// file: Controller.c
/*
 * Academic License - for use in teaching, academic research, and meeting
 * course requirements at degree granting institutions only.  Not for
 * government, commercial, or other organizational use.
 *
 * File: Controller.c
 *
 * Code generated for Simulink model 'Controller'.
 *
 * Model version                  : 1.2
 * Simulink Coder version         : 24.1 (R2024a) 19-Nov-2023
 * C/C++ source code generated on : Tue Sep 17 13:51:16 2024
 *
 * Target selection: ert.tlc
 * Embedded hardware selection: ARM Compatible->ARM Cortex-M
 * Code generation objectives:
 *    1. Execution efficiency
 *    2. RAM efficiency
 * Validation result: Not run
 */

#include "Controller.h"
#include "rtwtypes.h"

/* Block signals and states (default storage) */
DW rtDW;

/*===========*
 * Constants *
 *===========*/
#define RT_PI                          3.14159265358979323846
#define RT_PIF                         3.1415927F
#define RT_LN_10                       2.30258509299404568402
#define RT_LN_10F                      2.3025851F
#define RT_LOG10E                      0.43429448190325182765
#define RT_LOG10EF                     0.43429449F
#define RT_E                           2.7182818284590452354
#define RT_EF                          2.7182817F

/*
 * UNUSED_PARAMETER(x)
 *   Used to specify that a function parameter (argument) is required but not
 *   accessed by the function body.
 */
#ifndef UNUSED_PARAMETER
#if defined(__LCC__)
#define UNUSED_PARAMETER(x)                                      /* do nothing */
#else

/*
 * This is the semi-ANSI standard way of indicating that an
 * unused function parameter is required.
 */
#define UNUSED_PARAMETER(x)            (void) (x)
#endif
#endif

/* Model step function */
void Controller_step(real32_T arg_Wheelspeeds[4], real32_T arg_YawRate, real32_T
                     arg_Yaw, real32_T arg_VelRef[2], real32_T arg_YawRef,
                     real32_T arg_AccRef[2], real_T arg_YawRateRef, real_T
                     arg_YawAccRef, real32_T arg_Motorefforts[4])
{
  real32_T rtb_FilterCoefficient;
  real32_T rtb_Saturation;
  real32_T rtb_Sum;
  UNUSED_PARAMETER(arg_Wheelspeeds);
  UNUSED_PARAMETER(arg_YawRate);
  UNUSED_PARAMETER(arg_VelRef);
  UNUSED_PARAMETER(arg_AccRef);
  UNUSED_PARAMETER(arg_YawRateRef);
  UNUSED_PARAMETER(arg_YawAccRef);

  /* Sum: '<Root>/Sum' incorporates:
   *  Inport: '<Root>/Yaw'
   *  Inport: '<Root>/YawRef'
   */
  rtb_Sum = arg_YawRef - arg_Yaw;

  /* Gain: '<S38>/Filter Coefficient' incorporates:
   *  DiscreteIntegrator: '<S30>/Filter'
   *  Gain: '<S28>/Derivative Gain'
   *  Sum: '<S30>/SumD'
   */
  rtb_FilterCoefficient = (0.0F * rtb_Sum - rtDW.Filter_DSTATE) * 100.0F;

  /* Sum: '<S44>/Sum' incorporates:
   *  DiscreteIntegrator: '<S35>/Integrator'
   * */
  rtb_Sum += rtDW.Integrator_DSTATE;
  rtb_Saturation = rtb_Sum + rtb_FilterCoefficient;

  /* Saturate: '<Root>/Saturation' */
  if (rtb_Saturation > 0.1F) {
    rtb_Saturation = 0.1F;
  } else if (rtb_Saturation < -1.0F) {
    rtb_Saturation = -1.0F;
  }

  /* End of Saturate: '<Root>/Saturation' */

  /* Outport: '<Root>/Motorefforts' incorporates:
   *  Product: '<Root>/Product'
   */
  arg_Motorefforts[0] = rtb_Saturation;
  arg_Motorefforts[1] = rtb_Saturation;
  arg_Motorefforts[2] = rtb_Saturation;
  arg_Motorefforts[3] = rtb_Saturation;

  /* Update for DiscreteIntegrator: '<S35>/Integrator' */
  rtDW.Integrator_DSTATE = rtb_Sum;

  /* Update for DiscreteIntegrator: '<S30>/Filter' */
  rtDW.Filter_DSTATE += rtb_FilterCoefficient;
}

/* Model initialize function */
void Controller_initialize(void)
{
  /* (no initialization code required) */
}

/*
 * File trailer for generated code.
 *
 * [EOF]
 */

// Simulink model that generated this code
simulink model "Controller"  (R2024a)
settings: Solver=VariableStepAuto  StartTime=0.0  StopTime=10.0  RelTol=1e-3
libraries: slpidlib x1

== system Controller ==
  note: Reference
  note: Sensor inputs
  Wheelspeeds : Inport  OutDataTypeStr=single  Unit=rad/s  PortDimensions=4  LockScale=on
  YawRate : Inport  Port=2  OutDataTypeStr=single  Unit=rad/s  PortDimensions=1
  Yaw : Inport  Port=3  OutDataTypeStr=single  Unit=rad  PortDimensions=1
  VelRef : Inport  Port=4  OutDataTypeStr=single  Unit=m/s  PortDimensions=2
  YawRef : Inport  Port=5
  AccRef : Inport  Port=6  OutDataTypeStr=single  Unit=m/s^2  PortDimensions=2
  YawRateRef : Inport  Port=7
  YawAccRef : Inport  Port=8
  Discrete PID Controller : slpidlib/PID Controller  Controller=PID  Form=Parallel  TimeDomain=Discrete-time  UseExternalTs=off  SampleTime=-1  IntegratorMethod=Forward Euler  FilterMethod=Forward Euler  ControllerParametersSource=internal  P=1  I=1  UseKiTs=off  D=0  UseExternalDerivativeSource=off  N=100  UseFilter=on  TunerSelectOption=Transfer Function Based (PID Tuner App)  InitialConditionSource=internal  InitialConditionForIntegrator=0  InitialConditionForFilter=0  DifferentiatorICPrevScaledInput=0  ExternalReset=none  TrackingMode=off  Kt=1  LimitOutput=off  SatLimitsSource=internal  UpperSaturationLimit=inf  LowerSaturationLimit=-inf  LinearizeAsGain=off  AntiWindupMode=none  Kb=1  LimitIntegrator=off  UpperIntegratorSaturationLimit=inf  LowerIntegratorSaturationLimit=-inf  POutMin=[]  POutMax=[]  IOutMin=[]  IOutMax=[]  DOutMin=[]  DOutMax=[]  NOutMin=[]  NOutMax=[]  SumOutMin=[]  SumOutMax=[]  SaturationOutMin=[]  SaturationOutMax=[]  PParamMin=[]  PParamMax=[]  IParamMin=[]  IParamMax=[]  DParamMin=[]  DParamMax=[]  NParamMin=[]  NParamMax=[]  KbParamMin=[]  KbParamMax=[]  KtParamMin=[]  KtParamMax=[]  KbOutMin=[]  KbOutMax=[]  KtOutMin=[]  KtOutMax=[]  IntegratorOutMin=[]  IntegratorOutMax=[]  FilterOutMin=[]  FilterOutMax=[]  SumI1OutMin=[]  SumI1OutMax=[]  SumI2OutMin=[]  SumI2OutMax=[]  SumI3OutMin=[]  SumI3OutMax=[]  SumI4OutMin=[]  SumI4OutMax=[]  SumDOutMin=[]  SumDOutMax=[]  DifferentiatorOutMin=[]  DifferentiatorOutMax=[]  FilterDiffOutCoefMin=[]  FilterDiffOutCoefMax=[]  ReciprocalOutMin=[]  ReciprocalOutMax=[]  SumDenOutMin=[]  SumDenOutMax=[]  SumNumOutMin=[]  SumNumOutMax=[]  DivideOutMin=[]  DivideOutMax=[]  UdiffTsProdOutMin=[]  UdiffTsProdOutMax=[]  NTsProdOutMin=[]  NTsProdOutMax=[]  UintegralTsProdOutMin=[]  UintegralTsProdOutMax=[]  UngainTsProdOutMin=[]  UngainTsProdOutMax=[]  ClampingZeroOutDataTypeStr=Inherit: Inherit via back propagation  ClampingZeroOutMin=[]  ClampingZeroOutMax=[]  FilterDenConstantOutDataTypeStr=Inherit: Inherit via back propagation  FilterDenConstantOutMin=[]  FilterDenConstantOutMax=[]  PCopyOutDataTypeStr=Inherit: Inherit via back propagation  PCopyOutMin=[]  PCopyOutMax=[]  NCopyOutDataTypeStr=Inherit: Inherit via back propagation  NCopyOutMin=[]  NCopyOutMax=[]  IntegratorContinuousStateAttributes=''  IntegratorStateMustResolveToSignalObject=off  IntegratorRTWStateStorageClass=Auto  FilterContinuousStateAttributes=''  FilterStateMustResolveToSignalObject=off  FilterRTWStateStorageClass=Auto  ParallelPVariant=InternalParameters  IdealPVariant=Disabled  IVariant=InternalParameters  DVariant=InternalParameters  IntegratorVariant=Discrete  SatVariant=Disabled  AWVariant=Passthrough  PCopyVariant=Disabled  TRVariant=Disabled  FdbkBlocksVariant=Forward  IdealPFdbkVariant=Disabled  SatFdbkVariant=Disabled  DerivativeFilterVariant=ForwardEulerFilter  NVariant=InternalParameters  NCopyVariant=Disabled  FilterICVariant=InternalICsFilter  IntegratorICVariant=InternalICs  ExternalResetVariant=Disabled  TRSumVariant=Passthrough  SumFdbkVariant=Disabled  SumVariant=Sum_PID  TsampFilterVariant=InternalTs  TsampNgainVariant=Passthrough  TsampIntegralVariant=Disabled_SignalSpec  ExternalSaturationOutDataTypeStr=Inherit: Same as second input  DerivativeSourceVariant=ErrorSignal
  Expand Scalar : ExpandScalar  OutputDimensions=4  OutDataTypeStr=single
  Product : Product
  Saturation : Saturate  UpperLimit=0.1  LowerLimit=-01
  Sum : Sum  Inputs=|+-
  Motorefforts : Outport  OutDataTypeStr=single  PortDimensions=4
  wires:
  Sum/1 -> Discrete PID Controller/1
  YawRef/1 -> Sum/1
  Yaw/1 -> Sum/2
  Discrete PID Controller/1 -> Saturation/1
  Expand Scalar/1 -> Product/1
  Saturation/1 -> Product/2
  Product/1 -> Motorefforts/1
